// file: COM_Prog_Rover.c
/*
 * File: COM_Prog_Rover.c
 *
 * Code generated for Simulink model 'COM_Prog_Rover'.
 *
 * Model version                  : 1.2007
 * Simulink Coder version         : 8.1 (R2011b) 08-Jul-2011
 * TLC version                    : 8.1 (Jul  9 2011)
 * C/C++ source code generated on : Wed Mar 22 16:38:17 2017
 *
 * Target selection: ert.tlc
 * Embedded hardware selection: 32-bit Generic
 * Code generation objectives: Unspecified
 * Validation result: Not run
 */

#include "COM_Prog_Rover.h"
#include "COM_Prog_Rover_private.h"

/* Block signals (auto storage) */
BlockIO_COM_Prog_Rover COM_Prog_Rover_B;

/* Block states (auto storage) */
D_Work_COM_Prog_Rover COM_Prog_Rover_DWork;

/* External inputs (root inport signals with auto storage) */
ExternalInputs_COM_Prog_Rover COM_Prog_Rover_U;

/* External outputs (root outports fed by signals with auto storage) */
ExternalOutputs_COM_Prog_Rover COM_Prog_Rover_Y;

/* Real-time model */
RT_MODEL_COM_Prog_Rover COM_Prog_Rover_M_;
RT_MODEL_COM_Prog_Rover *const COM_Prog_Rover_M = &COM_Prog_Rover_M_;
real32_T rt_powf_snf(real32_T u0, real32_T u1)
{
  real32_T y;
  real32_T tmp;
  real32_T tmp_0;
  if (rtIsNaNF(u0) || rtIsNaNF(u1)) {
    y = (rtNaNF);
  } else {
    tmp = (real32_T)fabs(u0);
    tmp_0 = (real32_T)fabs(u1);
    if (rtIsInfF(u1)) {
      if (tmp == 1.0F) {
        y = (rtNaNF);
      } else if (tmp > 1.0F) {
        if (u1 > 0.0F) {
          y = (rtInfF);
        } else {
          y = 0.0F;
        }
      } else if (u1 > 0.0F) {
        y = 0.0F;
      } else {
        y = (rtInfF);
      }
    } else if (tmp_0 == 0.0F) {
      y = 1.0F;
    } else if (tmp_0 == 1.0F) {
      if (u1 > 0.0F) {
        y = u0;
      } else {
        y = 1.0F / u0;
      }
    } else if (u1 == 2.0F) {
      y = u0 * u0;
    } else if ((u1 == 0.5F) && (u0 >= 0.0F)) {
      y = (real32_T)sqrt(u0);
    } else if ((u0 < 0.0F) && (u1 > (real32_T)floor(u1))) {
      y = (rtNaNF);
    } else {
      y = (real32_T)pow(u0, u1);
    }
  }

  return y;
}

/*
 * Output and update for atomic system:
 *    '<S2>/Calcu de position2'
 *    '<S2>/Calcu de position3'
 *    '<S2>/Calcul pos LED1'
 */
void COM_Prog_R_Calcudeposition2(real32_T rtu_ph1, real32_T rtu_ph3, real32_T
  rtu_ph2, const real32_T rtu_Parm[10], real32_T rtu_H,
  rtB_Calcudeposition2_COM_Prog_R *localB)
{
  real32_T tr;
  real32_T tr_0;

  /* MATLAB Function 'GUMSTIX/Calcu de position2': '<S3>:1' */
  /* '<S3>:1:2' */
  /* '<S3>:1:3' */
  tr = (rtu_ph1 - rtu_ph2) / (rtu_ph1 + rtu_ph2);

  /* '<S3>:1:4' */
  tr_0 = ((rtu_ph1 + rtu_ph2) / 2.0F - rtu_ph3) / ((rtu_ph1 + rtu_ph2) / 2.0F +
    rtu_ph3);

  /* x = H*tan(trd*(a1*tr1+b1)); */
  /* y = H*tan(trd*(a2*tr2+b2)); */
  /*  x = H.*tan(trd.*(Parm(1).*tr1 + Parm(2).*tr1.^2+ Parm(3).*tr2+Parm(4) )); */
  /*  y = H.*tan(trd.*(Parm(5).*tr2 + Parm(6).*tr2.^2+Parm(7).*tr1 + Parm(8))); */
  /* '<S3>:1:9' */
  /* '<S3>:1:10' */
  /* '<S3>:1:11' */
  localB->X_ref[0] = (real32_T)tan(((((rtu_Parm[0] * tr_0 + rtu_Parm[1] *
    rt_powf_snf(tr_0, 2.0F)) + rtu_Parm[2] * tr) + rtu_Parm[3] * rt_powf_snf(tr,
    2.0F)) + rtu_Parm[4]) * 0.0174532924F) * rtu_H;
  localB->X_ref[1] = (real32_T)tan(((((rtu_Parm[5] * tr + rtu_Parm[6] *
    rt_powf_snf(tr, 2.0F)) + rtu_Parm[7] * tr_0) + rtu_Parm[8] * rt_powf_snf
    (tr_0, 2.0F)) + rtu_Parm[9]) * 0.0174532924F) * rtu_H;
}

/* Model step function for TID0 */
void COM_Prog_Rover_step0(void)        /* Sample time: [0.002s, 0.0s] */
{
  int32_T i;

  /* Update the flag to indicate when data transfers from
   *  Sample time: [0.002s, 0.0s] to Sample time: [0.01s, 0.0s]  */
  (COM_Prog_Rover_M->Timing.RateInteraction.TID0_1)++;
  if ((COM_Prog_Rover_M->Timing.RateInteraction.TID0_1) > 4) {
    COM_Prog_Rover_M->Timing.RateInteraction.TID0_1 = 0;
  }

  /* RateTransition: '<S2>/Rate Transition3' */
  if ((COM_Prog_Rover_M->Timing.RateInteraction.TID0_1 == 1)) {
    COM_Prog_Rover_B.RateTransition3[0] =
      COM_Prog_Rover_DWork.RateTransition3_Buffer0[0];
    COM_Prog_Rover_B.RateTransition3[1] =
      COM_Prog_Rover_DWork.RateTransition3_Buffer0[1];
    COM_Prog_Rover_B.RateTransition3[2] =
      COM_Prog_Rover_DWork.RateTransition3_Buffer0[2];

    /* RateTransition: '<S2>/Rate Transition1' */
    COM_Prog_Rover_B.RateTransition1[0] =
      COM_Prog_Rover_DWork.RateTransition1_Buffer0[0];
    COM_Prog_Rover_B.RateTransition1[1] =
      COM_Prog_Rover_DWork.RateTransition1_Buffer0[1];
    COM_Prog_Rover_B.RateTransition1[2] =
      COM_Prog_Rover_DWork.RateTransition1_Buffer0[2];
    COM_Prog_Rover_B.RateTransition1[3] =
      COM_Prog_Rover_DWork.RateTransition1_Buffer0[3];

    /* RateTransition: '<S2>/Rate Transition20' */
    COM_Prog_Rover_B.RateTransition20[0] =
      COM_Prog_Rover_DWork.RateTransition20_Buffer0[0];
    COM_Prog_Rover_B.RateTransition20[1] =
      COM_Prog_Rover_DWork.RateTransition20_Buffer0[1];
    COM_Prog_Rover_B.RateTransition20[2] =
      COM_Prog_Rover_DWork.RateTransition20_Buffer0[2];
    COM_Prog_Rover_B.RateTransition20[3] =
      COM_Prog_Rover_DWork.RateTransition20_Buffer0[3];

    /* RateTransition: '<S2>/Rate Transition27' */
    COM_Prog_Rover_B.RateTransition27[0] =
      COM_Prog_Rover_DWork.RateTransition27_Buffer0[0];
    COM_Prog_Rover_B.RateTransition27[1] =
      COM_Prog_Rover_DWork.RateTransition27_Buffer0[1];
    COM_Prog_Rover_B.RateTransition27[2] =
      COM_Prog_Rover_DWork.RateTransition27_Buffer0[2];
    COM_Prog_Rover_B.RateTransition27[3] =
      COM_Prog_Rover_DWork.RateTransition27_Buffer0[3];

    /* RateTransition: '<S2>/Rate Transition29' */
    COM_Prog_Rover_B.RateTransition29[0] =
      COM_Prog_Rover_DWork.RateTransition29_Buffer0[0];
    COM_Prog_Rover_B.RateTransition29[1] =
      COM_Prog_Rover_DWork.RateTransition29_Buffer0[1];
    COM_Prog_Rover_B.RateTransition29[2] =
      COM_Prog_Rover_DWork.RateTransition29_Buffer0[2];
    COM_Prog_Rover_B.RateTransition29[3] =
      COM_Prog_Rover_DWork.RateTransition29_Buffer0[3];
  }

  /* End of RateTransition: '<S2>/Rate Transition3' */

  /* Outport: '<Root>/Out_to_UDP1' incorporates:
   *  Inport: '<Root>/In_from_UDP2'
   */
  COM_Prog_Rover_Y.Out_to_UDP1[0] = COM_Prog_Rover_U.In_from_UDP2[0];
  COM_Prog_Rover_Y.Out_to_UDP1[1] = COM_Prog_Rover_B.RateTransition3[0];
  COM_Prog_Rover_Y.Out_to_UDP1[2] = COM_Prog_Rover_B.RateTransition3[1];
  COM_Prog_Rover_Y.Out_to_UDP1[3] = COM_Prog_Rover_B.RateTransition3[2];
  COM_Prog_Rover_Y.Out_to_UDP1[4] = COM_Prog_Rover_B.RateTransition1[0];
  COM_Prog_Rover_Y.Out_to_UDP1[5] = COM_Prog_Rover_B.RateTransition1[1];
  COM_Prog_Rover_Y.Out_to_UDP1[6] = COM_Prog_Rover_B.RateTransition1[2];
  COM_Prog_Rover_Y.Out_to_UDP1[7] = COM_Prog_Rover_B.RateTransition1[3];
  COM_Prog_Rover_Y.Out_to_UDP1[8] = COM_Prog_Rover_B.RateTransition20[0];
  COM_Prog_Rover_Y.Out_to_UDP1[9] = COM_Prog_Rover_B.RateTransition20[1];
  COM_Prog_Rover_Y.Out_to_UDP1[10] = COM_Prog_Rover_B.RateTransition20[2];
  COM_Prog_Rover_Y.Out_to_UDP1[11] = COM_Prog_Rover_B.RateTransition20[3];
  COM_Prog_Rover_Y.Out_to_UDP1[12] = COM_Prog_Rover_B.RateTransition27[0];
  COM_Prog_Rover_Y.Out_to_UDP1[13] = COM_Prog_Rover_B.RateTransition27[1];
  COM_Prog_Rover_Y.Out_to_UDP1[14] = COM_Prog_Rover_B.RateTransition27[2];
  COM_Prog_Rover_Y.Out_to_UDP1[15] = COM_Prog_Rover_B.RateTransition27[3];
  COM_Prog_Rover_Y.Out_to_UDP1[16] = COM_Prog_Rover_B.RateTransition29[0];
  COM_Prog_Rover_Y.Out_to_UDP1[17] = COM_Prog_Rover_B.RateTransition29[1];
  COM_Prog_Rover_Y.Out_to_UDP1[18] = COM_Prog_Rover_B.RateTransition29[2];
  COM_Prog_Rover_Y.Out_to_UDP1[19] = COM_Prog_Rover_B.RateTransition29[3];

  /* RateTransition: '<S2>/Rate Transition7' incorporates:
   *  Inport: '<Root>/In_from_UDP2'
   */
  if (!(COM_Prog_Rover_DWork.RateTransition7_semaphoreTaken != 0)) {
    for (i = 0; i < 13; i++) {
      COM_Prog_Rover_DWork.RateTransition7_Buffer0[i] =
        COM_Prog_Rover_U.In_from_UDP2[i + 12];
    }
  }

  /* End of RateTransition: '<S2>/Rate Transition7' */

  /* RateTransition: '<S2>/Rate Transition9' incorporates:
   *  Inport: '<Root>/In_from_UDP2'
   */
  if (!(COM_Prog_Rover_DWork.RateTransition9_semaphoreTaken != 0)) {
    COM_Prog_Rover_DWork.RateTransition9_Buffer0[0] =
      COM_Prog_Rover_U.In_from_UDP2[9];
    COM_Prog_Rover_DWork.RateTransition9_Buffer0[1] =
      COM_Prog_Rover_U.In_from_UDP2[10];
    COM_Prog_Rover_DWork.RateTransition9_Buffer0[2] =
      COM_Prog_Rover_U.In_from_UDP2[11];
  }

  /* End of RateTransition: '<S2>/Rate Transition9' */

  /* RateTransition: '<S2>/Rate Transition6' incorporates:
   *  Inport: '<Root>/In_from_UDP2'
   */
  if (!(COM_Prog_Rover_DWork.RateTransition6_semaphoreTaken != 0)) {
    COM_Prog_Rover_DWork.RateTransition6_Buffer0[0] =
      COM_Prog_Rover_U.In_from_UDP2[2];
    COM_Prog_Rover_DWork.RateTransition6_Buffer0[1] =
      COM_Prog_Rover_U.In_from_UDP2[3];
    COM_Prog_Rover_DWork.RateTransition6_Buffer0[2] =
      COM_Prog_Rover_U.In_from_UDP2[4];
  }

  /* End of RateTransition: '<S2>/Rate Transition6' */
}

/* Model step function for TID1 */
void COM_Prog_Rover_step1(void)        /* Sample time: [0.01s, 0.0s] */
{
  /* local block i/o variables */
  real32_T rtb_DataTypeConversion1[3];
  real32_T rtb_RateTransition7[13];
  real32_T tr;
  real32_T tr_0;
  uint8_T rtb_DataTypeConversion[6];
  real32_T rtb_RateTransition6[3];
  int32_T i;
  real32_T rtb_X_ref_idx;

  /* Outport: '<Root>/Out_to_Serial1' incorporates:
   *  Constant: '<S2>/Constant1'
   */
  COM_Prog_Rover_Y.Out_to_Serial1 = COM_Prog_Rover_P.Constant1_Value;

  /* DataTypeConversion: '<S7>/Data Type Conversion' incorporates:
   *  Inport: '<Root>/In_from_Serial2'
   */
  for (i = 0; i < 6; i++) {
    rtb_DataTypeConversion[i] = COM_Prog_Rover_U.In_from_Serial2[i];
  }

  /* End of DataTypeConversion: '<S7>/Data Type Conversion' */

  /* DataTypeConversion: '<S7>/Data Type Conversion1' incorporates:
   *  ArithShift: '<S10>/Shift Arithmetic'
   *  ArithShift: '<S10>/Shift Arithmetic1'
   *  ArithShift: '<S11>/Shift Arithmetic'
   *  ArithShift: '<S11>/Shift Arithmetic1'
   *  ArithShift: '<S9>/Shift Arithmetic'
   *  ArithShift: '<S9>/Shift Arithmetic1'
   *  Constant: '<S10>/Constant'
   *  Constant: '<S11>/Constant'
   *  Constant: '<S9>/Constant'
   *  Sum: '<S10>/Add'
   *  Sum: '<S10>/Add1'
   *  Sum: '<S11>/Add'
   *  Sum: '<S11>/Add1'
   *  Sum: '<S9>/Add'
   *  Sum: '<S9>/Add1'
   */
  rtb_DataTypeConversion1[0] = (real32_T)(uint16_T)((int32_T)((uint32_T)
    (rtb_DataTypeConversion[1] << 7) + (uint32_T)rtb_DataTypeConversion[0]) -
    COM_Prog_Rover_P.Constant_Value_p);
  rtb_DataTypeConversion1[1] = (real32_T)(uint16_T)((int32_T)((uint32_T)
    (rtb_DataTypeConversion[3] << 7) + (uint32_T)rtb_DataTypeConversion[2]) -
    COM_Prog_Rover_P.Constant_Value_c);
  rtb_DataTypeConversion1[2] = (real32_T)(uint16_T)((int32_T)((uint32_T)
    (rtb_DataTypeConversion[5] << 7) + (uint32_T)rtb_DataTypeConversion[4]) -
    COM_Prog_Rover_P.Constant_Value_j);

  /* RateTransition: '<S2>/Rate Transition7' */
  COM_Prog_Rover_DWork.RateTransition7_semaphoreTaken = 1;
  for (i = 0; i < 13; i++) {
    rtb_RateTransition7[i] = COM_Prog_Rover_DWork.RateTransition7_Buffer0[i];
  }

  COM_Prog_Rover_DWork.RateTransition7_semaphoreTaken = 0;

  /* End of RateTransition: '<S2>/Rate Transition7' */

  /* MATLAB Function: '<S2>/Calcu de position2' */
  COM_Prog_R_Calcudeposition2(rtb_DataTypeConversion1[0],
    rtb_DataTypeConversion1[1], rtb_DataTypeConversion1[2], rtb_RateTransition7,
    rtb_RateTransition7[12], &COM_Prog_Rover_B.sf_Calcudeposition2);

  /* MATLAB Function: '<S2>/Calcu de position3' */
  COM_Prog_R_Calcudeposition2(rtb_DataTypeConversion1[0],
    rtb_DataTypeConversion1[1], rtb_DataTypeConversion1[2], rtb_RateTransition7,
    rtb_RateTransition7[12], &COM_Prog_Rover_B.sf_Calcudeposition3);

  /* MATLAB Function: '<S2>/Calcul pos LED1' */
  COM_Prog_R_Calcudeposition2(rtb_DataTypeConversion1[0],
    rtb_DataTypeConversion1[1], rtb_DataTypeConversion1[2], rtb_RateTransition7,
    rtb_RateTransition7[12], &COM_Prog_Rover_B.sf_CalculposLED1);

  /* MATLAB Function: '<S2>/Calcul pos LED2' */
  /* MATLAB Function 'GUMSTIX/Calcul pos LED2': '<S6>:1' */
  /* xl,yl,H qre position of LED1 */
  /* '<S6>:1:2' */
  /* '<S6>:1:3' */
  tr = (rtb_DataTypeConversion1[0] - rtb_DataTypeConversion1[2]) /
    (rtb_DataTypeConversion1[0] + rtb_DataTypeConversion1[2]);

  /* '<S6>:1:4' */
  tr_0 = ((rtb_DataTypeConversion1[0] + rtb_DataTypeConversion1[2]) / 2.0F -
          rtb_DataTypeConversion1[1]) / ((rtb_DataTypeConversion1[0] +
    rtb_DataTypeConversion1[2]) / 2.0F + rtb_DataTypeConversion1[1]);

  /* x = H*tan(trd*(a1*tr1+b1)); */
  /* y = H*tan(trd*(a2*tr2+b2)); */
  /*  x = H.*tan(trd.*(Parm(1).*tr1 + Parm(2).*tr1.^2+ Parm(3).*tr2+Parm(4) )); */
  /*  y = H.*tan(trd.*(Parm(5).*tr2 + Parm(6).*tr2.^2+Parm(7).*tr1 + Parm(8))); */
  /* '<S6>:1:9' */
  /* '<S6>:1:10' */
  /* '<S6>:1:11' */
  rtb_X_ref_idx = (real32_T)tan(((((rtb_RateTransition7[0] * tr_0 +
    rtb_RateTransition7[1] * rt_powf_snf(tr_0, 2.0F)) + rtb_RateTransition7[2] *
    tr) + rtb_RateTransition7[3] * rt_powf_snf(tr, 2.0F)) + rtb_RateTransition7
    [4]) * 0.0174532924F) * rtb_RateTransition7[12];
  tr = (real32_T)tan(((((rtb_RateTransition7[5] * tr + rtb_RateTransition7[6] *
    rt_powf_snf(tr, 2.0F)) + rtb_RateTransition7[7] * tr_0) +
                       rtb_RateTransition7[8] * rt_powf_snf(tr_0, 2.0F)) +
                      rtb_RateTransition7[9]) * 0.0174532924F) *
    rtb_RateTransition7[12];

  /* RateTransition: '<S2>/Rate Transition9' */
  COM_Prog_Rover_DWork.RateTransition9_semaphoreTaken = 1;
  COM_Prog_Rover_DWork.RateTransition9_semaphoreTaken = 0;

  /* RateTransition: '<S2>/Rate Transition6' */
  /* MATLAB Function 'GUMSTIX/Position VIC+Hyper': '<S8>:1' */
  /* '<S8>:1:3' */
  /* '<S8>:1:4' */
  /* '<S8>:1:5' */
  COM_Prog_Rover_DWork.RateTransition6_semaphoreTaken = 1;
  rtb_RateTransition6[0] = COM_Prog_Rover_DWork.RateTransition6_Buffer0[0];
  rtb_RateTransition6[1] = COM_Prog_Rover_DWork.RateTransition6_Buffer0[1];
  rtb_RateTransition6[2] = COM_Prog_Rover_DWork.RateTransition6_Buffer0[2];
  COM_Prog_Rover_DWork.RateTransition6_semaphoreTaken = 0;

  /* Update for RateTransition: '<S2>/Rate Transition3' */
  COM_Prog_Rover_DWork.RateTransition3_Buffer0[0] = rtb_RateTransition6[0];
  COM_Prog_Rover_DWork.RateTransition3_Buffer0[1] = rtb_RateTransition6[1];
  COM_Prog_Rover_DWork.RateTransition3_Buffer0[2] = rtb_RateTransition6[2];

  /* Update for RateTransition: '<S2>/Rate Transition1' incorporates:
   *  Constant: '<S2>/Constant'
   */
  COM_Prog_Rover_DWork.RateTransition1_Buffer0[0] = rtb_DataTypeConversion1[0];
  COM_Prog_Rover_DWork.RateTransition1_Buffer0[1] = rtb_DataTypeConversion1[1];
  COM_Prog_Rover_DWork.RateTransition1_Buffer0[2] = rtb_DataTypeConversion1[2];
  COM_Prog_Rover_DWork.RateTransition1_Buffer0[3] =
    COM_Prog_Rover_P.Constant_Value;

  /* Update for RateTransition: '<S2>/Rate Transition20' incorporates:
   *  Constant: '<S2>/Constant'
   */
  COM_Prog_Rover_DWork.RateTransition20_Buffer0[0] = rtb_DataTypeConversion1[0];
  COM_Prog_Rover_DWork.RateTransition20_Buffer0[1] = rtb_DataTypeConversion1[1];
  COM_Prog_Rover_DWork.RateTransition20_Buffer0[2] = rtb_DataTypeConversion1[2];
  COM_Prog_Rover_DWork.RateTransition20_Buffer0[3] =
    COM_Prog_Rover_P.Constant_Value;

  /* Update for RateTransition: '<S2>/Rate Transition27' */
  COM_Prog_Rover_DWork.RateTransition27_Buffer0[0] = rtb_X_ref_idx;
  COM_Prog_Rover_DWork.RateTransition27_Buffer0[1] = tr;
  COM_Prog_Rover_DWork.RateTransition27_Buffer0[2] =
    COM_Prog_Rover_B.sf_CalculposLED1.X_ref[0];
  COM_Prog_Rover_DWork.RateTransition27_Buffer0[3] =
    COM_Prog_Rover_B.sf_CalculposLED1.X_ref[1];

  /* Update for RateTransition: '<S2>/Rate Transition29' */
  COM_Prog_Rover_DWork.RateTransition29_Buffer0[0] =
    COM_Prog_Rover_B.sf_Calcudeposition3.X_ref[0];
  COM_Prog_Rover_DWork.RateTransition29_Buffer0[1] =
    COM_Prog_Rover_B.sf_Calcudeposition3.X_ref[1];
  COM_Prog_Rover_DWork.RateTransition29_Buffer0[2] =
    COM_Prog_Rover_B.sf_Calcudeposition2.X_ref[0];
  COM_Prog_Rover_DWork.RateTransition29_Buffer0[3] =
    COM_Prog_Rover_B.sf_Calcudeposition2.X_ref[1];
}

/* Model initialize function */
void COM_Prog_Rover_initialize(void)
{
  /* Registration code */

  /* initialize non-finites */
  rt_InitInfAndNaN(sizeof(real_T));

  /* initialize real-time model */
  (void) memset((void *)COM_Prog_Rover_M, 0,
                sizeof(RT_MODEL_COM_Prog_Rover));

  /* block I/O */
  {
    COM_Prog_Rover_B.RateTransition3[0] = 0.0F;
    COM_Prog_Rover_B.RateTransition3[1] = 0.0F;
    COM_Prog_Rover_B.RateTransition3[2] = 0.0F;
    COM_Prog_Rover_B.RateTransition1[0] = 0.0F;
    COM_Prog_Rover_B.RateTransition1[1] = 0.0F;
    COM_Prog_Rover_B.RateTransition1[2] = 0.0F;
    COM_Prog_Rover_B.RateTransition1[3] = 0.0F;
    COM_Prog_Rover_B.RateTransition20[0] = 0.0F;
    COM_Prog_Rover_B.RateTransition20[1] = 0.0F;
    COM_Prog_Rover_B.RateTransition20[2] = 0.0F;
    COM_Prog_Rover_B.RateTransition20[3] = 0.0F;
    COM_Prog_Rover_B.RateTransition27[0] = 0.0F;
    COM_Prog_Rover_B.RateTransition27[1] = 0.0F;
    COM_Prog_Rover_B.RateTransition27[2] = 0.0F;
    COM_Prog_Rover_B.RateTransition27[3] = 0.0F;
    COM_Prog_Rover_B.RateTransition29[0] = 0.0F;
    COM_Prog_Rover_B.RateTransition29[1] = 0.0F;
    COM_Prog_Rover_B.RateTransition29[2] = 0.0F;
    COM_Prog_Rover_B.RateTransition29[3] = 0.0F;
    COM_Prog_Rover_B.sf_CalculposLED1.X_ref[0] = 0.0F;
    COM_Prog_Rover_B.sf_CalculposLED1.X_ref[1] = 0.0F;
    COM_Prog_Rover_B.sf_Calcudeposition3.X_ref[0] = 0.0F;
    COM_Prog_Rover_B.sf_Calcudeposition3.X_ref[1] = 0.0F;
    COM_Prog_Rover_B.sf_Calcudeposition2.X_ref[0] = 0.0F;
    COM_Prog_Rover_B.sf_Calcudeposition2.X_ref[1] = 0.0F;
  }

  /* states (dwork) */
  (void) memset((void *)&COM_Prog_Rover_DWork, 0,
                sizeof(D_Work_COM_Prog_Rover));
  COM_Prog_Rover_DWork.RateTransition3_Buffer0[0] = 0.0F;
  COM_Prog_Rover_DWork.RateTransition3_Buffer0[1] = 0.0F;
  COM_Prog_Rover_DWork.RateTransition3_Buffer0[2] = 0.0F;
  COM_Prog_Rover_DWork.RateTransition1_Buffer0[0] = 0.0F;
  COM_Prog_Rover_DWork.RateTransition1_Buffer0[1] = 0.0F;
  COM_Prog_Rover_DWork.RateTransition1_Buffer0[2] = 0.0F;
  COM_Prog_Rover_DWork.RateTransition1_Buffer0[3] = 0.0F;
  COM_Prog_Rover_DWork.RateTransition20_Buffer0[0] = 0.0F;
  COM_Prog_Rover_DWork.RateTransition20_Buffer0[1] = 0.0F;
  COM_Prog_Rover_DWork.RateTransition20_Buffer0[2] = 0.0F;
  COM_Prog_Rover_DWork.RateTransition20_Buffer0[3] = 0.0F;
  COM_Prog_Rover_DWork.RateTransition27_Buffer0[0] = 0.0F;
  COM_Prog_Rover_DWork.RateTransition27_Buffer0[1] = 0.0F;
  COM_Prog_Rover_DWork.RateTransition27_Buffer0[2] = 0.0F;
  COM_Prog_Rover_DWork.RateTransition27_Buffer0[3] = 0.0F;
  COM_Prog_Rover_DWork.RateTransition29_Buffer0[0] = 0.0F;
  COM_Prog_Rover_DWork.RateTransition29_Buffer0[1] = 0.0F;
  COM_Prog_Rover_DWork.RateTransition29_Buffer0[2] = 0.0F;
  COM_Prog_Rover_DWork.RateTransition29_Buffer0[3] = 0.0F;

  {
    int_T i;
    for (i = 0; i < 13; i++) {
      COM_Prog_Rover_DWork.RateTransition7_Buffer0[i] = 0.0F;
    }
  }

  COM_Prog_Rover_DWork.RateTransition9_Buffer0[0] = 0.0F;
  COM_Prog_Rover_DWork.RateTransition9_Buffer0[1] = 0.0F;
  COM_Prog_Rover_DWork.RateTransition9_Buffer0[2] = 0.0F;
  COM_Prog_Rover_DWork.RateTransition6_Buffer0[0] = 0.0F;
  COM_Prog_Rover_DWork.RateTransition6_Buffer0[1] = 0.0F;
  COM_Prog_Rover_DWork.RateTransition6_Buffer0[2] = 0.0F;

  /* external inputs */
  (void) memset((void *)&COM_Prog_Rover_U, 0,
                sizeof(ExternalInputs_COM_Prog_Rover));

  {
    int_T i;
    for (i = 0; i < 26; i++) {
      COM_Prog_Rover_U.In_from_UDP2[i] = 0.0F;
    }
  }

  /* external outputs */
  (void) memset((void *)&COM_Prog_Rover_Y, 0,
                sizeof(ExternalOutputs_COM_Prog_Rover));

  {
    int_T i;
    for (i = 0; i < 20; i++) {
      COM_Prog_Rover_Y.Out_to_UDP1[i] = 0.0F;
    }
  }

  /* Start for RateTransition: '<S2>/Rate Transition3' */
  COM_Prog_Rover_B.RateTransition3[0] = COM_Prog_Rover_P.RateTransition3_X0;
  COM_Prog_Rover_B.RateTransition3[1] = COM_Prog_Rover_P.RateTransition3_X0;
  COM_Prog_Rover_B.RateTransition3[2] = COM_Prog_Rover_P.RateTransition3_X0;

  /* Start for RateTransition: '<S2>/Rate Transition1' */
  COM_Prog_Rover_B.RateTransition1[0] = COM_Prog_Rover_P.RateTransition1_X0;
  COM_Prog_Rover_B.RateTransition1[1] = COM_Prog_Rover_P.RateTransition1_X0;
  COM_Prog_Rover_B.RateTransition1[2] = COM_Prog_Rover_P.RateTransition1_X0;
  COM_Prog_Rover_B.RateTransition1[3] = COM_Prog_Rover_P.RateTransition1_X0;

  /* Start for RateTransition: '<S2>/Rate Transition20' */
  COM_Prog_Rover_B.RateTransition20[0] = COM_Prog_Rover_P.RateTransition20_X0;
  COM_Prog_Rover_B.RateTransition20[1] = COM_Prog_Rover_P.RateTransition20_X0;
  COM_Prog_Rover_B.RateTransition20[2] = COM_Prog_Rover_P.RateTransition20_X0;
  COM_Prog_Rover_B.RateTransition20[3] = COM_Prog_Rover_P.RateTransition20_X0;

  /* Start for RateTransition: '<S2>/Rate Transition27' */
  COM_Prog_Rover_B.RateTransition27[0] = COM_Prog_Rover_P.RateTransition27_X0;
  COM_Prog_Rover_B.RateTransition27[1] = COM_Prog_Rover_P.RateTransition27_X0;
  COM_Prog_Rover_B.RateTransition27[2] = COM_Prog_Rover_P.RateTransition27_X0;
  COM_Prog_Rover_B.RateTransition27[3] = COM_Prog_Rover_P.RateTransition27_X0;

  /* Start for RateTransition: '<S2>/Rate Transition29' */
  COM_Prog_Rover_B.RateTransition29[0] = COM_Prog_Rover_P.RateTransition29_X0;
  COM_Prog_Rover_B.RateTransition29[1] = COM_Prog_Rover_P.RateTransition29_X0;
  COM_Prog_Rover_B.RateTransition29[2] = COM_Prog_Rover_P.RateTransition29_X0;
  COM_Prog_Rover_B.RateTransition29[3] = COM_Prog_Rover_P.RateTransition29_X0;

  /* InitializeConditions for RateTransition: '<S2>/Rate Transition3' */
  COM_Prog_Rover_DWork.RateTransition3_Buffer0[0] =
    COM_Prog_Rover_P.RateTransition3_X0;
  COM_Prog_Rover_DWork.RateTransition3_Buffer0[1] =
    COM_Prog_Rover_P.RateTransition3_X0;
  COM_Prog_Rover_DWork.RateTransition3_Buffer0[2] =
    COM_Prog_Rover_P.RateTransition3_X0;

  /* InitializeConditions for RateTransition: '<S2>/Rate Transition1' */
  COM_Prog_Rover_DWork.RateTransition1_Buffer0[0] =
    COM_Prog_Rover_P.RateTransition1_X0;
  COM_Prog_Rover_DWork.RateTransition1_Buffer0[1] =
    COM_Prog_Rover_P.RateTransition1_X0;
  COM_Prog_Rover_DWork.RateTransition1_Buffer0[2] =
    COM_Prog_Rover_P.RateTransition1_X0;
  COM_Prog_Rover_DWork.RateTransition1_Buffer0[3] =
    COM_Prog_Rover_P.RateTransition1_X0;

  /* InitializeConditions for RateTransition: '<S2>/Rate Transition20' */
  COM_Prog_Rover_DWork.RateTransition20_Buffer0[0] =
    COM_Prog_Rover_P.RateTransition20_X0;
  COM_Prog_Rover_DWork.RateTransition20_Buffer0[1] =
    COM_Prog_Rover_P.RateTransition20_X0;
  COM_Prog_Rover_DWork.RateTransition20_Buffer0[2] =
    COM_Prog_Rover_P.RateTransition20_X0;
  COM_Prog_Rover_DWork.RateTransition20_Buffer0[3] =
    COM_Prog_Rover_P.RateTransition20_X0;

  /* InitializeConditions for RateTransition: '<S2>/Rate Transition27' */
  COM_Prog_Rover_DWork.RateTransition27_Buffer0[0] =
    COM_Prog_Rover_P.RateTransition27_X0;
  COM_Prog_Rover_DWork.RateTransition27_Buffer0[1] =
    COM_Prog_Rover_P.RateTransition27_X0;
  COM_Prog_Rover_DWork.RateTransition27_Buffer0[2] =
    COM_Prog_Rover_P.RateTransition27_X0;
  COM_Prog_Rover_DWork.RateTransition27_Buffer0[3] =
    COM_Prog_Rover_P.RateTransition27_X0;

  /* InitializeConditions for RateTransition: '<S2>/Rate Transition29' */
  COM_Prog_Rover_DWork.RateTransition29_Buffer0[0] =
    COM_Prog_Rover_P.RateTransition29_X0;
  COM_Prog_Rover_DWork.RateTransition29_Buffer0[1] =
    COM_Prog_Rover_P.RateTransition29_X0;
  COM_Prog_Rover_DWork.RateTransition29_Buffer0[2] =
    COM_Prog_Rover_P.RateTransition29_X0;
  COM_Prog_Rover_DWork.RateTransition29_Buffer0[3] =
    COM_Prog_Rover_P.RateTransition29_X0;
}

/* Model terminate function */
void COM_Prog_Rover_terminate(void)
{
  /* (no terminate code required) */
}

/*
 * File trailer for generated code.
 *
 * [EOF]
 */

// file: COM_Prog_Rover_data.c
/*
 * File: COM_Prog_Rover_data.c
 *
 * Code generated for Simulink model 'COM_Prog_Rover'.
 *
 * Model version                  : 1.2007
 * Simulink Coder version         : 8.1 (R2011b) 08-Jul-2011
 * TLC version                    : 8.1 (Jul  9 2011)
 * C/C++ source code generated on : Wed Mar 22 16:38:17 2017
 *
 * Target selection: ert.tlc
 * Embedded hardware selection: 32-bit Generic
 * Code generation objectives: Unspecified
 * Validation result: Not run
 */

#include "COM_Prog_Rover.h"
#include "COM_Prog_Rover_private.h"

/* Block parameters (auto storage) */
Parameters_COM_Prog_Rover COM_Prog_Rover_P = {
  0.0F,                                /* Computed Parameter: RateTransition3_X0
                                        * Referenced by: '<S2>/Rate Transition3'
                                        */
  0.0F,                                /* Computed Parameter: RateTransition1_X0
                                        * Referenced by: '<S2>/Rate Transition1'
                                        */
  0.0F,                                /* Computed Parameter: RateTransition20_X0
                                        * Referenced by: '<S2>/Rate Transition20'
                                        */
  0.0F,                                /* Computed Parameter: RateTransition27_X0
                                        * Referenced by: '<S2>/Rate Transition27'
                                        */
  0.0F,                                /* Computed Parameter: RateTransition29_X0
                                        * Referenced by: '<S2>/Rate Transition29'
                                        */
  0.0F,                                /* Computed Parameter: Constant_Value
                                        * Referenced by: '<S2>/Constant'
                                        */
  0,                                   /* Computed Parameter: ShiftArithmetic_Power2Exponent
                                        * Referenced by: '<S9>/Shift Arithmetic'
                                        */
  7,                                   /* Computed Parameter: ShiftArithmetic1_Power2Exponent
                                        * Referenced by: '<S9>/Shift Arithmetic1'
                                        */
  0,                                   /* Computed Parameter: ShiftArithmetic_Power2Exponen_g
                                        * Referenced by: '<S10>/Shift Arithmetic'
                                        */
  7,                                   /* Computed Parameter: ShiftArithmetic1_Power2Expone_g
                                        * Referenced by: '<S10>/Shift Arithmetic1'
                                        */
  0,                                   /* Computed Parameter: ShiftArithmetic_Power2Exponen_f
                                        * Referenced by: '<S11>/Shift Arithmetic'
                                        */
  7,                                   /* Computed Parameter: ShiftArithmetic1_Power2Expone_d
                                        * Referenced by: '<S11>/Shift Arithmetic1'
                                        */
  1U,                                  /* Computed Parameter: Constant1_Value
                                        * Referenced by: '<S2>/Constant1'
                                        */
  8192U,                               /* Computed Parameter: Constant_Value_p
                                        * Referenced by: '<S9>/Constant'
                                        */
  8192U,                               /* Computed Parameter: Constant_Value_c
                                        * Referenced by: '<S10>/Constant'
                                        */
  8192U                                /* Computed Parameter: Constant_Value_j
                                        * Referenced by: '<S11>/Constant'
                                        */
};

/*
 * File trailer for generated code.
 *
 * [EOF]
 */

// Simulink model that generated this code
simulink model "COM_Prog_Rover"  (Simulink 7.8)
settings: Solver=FixedStepDiscrete  StartTime=0.0  StopTime=inf  FixedStep=ComMinSampleTime  RelTol=1e-3
undefined symbols (not defined in the file or in its folder): ComMinSampleTime, Gumstix

== system COM_Prog_Rover ==
  In_from_UDP2 : Inport  OutDataTypeStr=single  PortDimensions=Gumstix.UDP.Reception(1).NbData  SampleTime=Gumstix.UDP.Reception(1).SampleTime  mask{UDP_NbData=26, UDP_DataType=float32, UDP_remoteIPaddress='192.168.137.3', UDP_remotePort=2012, UDP_Interface=wlan0, UDP_localPort=2012, UDP_SampleTime=ComMinSampleTime, UDP_BlockingReception=OFF (try to read the n data), UDP_BlockingTimeOut=0.1}
      mask prompts: UDP_NbData "Number of Received Data"; UDP_DataType "UDP Data Type"; UDP_remoteIPaddress "Remote peer's IP address (IPv4)"; UDP_remotePort "Remote peer's Port (1023<port<65536)"; UDP_Interface "Local Interface to use"; UDP_localPort "Local Port (1023<port<65536)"; UDP_SampleTime "Reception Sample Time [s]"; UDP_BlockingReception "Blocking Reception"; UDP_BlockingTimeOut "Blocking Time Out [s]"
      mask init:
      | for i=1:1:8
      |     ProcessUDPInportMask_COM(gcb, i);
      | end
  In_from_Serial2 : Inport  Port=2  OutDataTypeStr=uint8  PortDimensions=Gumstix.RS232.Reception(1).NbData  SampleTime=Gumstix.RS232.Reception(1).SampleTime  mask{RS232_NbData=6, RS232_DataType=unsigned char8, RS232_Port=/dev/ttyO0, RS232_BaudRate=115200, RS232_SampleTime=0.01, RS232_BlockingReception=OFF (try to read the n data), RS232_BlockingTimeOut=0.00022, RS232_StreamHeaderReception=1 byte, RS232_StreamHeaderValue=174, RS232_StartProtocol=SendStart -> WaitStart, RS232_StartTimeOut=100, RS232_StartStream=START, RS232_StopProtocol=None, RS232_StopTimeOut=100, RS232_StopStream=STOP}
      mask prompts: RS232_NbData "Number of Received Data"; RS232_DataType "RS232 Data Type"; RS232_Port "Serial Port"; RS232_BaudRate "BaudRate"; RS232_SampleTime "Reception Sample Time [s]"; RS232_BlockingReception "Blocking Reception"; RS232_BlockingTimeOut "Blocking Time Out [s]"; RS232_StreamHeaderReception "Stream Header"; RS232_StreamHeaderValue "Stream header value [0-255]"; RS232_StartProtocol "START Protocols"; RS232_StartTimeOut "Start Stream Waiting TimeOut [ms]"; RS232_StartStream "Start Message"; RS232_StopProtocol "STOP Protocols"; RS232_StopTimeOut "Stop Stream Waiting TimeOut [ms]"; RS232_StopStream "Stop Message"
      mask init:
      | for i=1:1:15
      |     ProcessRS232InportMask_COM(gcb, i);
      | end
  DisplaySampleTimeColors : Subsystem  mask{SampleTime_1=0.002, SampleTime_2=0.004, SampleTime_3=0.01}
  GUMSTIX : Subsystem
  Gumstix Configuration : Subsystem  mask{TimeSynchro=Internal Clock, RS232_InterruptSource=/dev/ttyO0, UDP_InterruptSource=wlan0, PrintfMode=off, FprintfMode=off, TimeLoggerMode=off, PrintfTimeMode=off, FprintfTimeMode=off, TaskingMode=Multi-Tasking, SchedPolicy=SCHED_RR        (Real-Time Scheduler), MaxTaskPriority=96, RTsystem=PREEMPT-RT}
      mask prompts: TimeSynchro "Time Scheduler"; RS232_InterruptSource "RS232 Interrupt Source"; UDP_InterruptSource "UDP Interrupt Source"; PrintfMode "Verbose mode activated in the Gumstix console"; FprintfMode "Verbose mode logged in a file (onto Gumstix)"; TimeLoggerMode "Time logger mode activated (log time exec of each task)"; PrintfTimeMode "Execution time plotted in the Gumstix console"; FprintfTimeMode "Execution time logged in a file (onto Gumstix)"; TaskingMode "Tasking Mode"; SchedPolicy "Scheduler Policy"; MaxTaskPriority "Maximum Task Priority [1-99]"; RTsystem "RT system"
      mask init:
      | for i=1:1:12
      |     ProcessConfigMask_COM(gcb, i);
      | end
  Out_to_UDP1 : Outport  OutDataTypeStr=single  PortDimensions=Gumstix.UDP.Emission(1).NbData  SampleTime=Gumstix.UDP.Emission(1).SampleTime  mask{UDP_NbData=20, UDP_DataType=float32, UDP_RemoteIPaddress='192.168.137.3', UDP_RemotePort=2012, UDP_Interface=wlan0, UDP_LocalPort=2012, UDP_SampleTime=ComMinSampleTime}
      mask prompts: UDP_NbData "Number of Sent Data"; UDP_DataType "UDP Data Type"; UDP_RemoteIPaddress "remote peer's IP address (IPv4)"; UDP_RemotePort "remote peer's Port (1023<port<65536)"; UDP_Interface "Local Interface to use for UDP"; UDP_LocalPort "Local port to use"; UDP_SampleTime "Emission Sample Time [s]"
      mask init:
      | for i=1:1:7
      |     ProcessUDPOutportMask_COM(gcb, i);
      | end
  Out_to_Serial1 : Outport  Port=2  OutDataTypeStr=uint16  PortDimensions=Gumstix.RS232.Emission(1).NbData  SampleTime=Gumstix.RS232.Emission(1).SampleTime  mask{RS232_NbData=1, RS232_DataType=unsigned int16, RS232_Port=/dev/ttyO0, RS232_BaudRate=115200, RS232_SampleTime=0.01, RS232_StreamHeaderReception=1 byte, RS232_StreamHeaderValue=174, RS232_StartProtocol=SendStart -> WaitStart, RS232_StartTimeOut=100, RS232_StartStream=START, RS232_StopProtocol=None, RS232_StopTimeOut=100, RS232_StopStream=STOP}
      mask prompts: RS232_NbData "Number of Sent Data"; RS232_DataType "RS232 Data Type"; RS232_Port "Serial Port"; RS232_BaudRate "BaudRate"; RS232_SampleTime "Sample Time [s]"; RS232_StreamHeaderReception "Stream Header"; RS232_StreamHeaderValue "Stream header value [0-255]"; RS232_StartProtocol "RS232 Start Protocol"; RS232_StartTimeOut "Start Stream Waiting TimeOut [ms]"; RS232_StartStream "Start Message"; RS232_StopProtocol "RS232 Stop Protocol"; RS232_StopTimeOut "Stop Stream Waiting TimeOut [ms]"; RS232_StopStream "Stop Message"
      mask init:
      | for i=1:1:13
      |     ProcessRS232OutportMask_COM(gcb, i);
      | end
  wires:
  GUMSTIX/1(Out_to_UDP) -> Out_to_UDP1/1
  In_from_UDP2/1 -> GUMSTIX/1(In_from_UDP)
  In_from_Serial2/1 -> GUMSTIX/2("In_from_Serial2 ")
  GUMSTIX/2(Out_to_Serial) -> Out_to_Serial1/1

== system COM_Prog_Rover/DisplaySampleTimeColors ==
  Constant : Constant  OutDataTypeStr=uint8
  Gain : Gain
  Terminator : Terminator
  wires:
  Constant/1 -> Gain/1
  Gain/1 -> Terminator/1

== system COM_Prog_Rover/GUMSTIX ==
  note: enable rotation detec
  note: 0.002
  note: 0.002
  note: 0.01
  note: 0.01
  note: 0.01
  note: 0.01
  note: 0.01
  note: ??
  In_from_UDP : Inport
  "In_from_Serial2 " : Inport  Port=2
  Calcu de position2 : MATLAB Function  TreatAsAtomicUnit=on
  Calcu de position3 : MATLAB Function  TreatAsAtomicUnit=on
  Calcul pos LED1 : MATLAB Function  TreatAsAtomicUnit=on
  Calcul pos LED2 : MATLAB Function  TreatAsAtomicUnit=on
  Constant : Constant  Value=0  OutDataTypeStr=Inherit: Inherit via back propagation  SampleTime=0.01
  Constant1 : Constant  OutDataTypeStr=Inherit: Inherit via back propagation  SampleTime=0.01
  Data Type Conversion2 : DataTypeConversion
  Data Type Conversion3 : DataTypeConversion
  Data Type Conversion5 : DataTypeConversion
  Decode1 : Subsystem
  Demux : Demux  Outputs=[2 1]
  Demux{1,4,9,12} (4 alike) : Demux  Outputs=[10 1 1 1]
  Demux10 : Demux  Outputs=[ 1 1 1 1]
  Demux13 : Demux  Outputs=[ 1 1 1 1]
  Demux18 : Demux  Outputs=[1 1]
  Demux2 : Demux  Outputs=[1 1 1 1]
  Demux5 : Demux  Outputs=[1 1 1 1]
  In_from_UDP_Demux : Demux  Outputs=[1 1 3 3 1 3 13 1]
  Mux : Mux  Inputs=2
  Mux2 : Mux  Inputs=2
  Mux4 : Mux  Inputs=2
  Out_to_UDP_Mux : Mux  Inputs=[1 3 4 4 4 4]
  Position VIC+Hyper : MATLAB Function  TreatAsAtomicUnit=on
  Rate Transition{1,3,20,27,29} (5 alike) : RateTransition
  Rate Transition2 : RateTransition  Deterministic=off
  Rate Transition{6..7,9,23,31} (5 alike) : RateTransition  Deterministic=off  OutPortSampleTime=Ts_control
  Rate Transition24 : RateTransition  Deterministic=off
  Out_to_UDP : Outport
  Out_to_Serial : Outport  Port=2
  wires:
  In_from_UDP/1 -> Rate Transition2/1
  Rate Transition2/1 -> Data Type Conversion3/1
  Data Type Conversion3/1 -> In_from_UDP_Demux/1
  In_from_UDP_Demux/1 -> [Compteur]
  In_from_UDP_Demux/2 -> [Mode]
  Rate Transition9/1 -> [States]
  [References] -> Rate Transition3/1
  Rate Transition6/1 -> [References]
  Rate Transition23/1 -> [X_mes]
  Rate Transition24/1 -> [Int_reset]
  Rate Transition3/1 -> Out_to_UDP_Mux/2
  Demux1/1 -> Calcul pos LED1/4(Parm)
  Rate Transition7/1 -> [par_loc]
  Demux1/2 -> Calcul pos LED1/5(xl)
  Demux1/3 -> Calcul pos LED1/6(yl)
  Demux1/4 -> [H], Calcul pos LED1/7(H)
  [Capteur2] -> Rate Transition20/1
  [par_loc] -> Demux4/1
  Demux4/1 -> Calcul pos LED2/4(Parm)
  Demux4/2 -> Calcul pos LED2/5(xl)
  Demux4/3 -> Calcul pos LED2/6(yl)
  Demux4/4 -> Calcul pos LED2/7(H)
  [Capteur2] -> Demux2/1
  Calcul pos LED2/1(X_ref) -> [X_est_2]
  [Compteur] -> Out_to_UDP_Mux/1
  Out_to_UDP_Mux/1 -> Out_to_UDP/1
  [X_est_2] -> Mux2/1
  Mux2/1 -> Data Type Conversion2/1
  Data Type Conversion2/1 -> Rate Transition27/1
  [X_est_1] -> Mux2/2
  Position VIC+Hyper/1(X_new) -> [X_mes_hybride]
  [Capteur1] -> Rate Transition1/1
  [States] -> Demux/1
  Demux9/1 -> Calcu de position2/4(Parm)
  [par_loc] -> Demux9/1
  Demux9/2 -> Calcu de position2/5(xl)
  Demux9/3 -> Calcu de position2/6(yl)
  Demux9/4 -> Calcu de position2/7(H)
  [Capteur1] -> Demux13/1
  [par_loc] -> Demux12/1
  Demux12/1 -> Calcu de position3/4(Parm)
  Demux12/2 -> Calcu de position3/5(xl)
  Demux12/3 -> Calcu de position3/6(yl)
  Demux12/4 -> Calcu de position3/7(H)
  [Capteur2] -> Demux10/1
  Calcu de position3/1(X_ref) -> [X_est_2_b]
  Demux10/1 -> Calcu de position3/1(ph1)
  Demux10/2 -> Calcu de position3/2(ph3)
  Demux10/3 -> Calcu de position3/3(ph2)
  Demux13/1 -> Calcu de position2/1(ph1)
  Demux13/2 -> Calcu de position2/2(ph3)
  Demux13/3 -> Calcu de position2/3(ph2)
  Calcul pos LED1/1(X_ref) -> Demux18/1, [X_est_1]
  [X_est_2_b] -> Mux4/1
  Mux4/1 -> Data Type Conversion5/1
  Data Type Conversion5/1 -> Rate Transition29/1
  [X_est_1_b] -> Mux4/2
  Rate Transition31/1 -> [d]
  Demux18/2 -> Position VIC+Hyper/2(y_hyp)
  Demux18/1 -> Position VIC+Hyper/1(x_hyp)
  Demux/2 -> Position VIC+Hyper/3(phi_vic)
  [par_loc] -> Demux1/1
  [Capteur1] -> Demux5/1
  Calcu de position2/1(X_ref) -> [X_est_1_b]
  Rate Transition1/1 -> Out_to_UDP_Mux/3
  In_from_UDP_Demux/3 -> Rate Transition6/1
  In_from_UDP_Demux/4 -> Rate Transition23/1
  In_from_UDP_Demux/5 -> Rate Transition24/1
  In_from_UDP_Demux/6 -> Rate Transition9/1
  In_from_UDP_Demux/7 -> Rate Transition7/1
  In_from_UDP_Demux/8 -> Rate Transition31/1
  Rate Transition20/1 -> Out_to_UDP_Mux/4
  Rate Transition27/1 -> Out_to_UDP_Mux/5
  Rate Transition29/1 -> Out_to_UDP_Mux/6
  "In_from_Serial2 "/1 -> Decode1/1(In1)
  Decode1/1(Out1) -> Mux/1
  Constant/1 -> Mux/2
  Mux/1 -> [Capteur1], [Capteur2]
  Demux2/1 -> Calcul pos LED2/1(ph1)
  Demux2/2 -> Calcul pos LED2/2(ph3)
  Demux2/3 -> Calcul pos LED2/3(ph2)
  Demux5/1 -> Calcul pos LED1/1(ph1)
  Demux5/2 -> Calcul pos LED1/2(ph3)
  Demux5/3 -> Calcul pos LED1/3(ph2)
  Constant1/1 -> Out_to_Serial/1

== system COM_Prog_Rover/Gumstix Configuration ==

== system COM_Prog_Rover/GUMSTIX/Decode1 ==
  In1 : Inport
  Data Type Conversion : DataTypeConversion  OutDataTypeStr=uint16
  Data Type Conversion1 : DataTypeConversion  OutDataTypeStr=single
  Demux : Demux  Outputs=6
  Mux : Mux  Inputs=3
  Subsystem : Subsystem
  Subsystem1 : Subsystem
  Subsystem2 : Subsystem
  Out1 : Outport
  wires:
  Data Type Conversion1/1 -> Out1/1
  In1/1 -> Data Type Conversion/1
  Data Type Conversion/1 -> Demux/1
  Demux/1 -> Subsystem/1(In1)
  Demux/2 -> Subsystem/2(In2)
  Demux/3 -> Subsystem1/1(In1)
  Demux/4 -> Subsystem1/2(In2)
  Demux/5 -> Subsystem2/1(In1)
  Demux/6 -> Subsystem2/2(In2)
  Subsystem/1(Out1) -> Mux/1
  Subsystem1/1(Out1) -> Mux/2
  Subsystem2/1(Out1) -> Mux/3
  Mux/1 -> Data Type Conversion1/1

== system COM_Prog_Rover/GUMSTIX/Decode1/Subsystem ==
  In1 : Inport
  In2 : Inport  Port=2
  Add : Sum
  Add1 : Sum  Inputs=+-
  Constant : Constant  Value=2^13  OutDataTypeStr=uint16  SampleTime=-1
  Shift Arithmetic : ArithShift  BitShiftDirection=Right
  Shift Arithmetic1 : ArithShift  BitShiftNumber=7  BitShiftDirection=Left
  Out1 : Outport
  wires:
  In1/1 -> Shift Arithmetic/1
  In2/1 -> Shift Arithmetic1/1
  Shift Arithmetic/1 -> Add/1
  Shift Arithmetic1/1 -> Add/2
  Add/1 -> Add1/1
  Constant/1 -> Add1/2
  Add1/1 -> Out1/1

== system COM_Prog_Rover/GUMSTIX/Decode1/Subsystem1 ==
  In1 : Inport
  In2 : Inport  Port=2
  Add : Sum
  Add1 : Sum  Inputs=+-
  Constant : Constant  Value=2^13  OutDataTypeStr=uint16  SampleTime=-1
  Shift Arithmetic : ArithShift  BitShiftDirection=Right
  Shift Arithmetic1 : ArithShift  BitShiftNumber=7  BitShiftDirection=Left
  Out1 : Outport
  wires:
  In1/1 -> Shift Arithmetic/1
  In2/1 -> Shift Arithmetic1/1
  Shift Arithmetic/1 -> Add/1
  Shift Arithmetic1/1 -> Add/2
  Add/1 -> Add1/1
  Constant/1 -> Add1/2
  Add1/1 -> Out1/1

== system COM_Prog_Rover/GUMSTIX/Decode1/Subsystem2 ==
  In1 : Inport
  In2 : Inport  Port=2
  Add : Sum
  Add1 : Sum  Inputs=+-
  Constant : Constant  Value=2^13  OutDataTypeStr=uint16  SampleTime=-1
  Shift Arithmetic : ArithShift  BitShiftDirection=Right
  Shift Arithmetic1 : ArithShift  BitShiftNumber=7  BitShiftDirection=Left
  Out1 : Outport
  wires:
  In1/1 -> Shift Arithmetic/1
  In2/1 -> Shift Arithmetic1/1
  Shift Arithmetic/1 -> Add/1
  Shift Arithmetic1/1 -> Add/2
  Add/1 -> Add1/1
  Constant/1 -> Add1/2
  Add1/1 -> Out1/1

== matlab function GUMSTIX/Calcul pos LED2 ==
function X_ref = position(ph1, ph3, ph2, Parm, xl, yl, H)   %xl,yl,H qre position of LED1
trd = pi/180;
tr2 = (ph1-ph2)/(ph1+ph2);
tr1 = (((ph1+ph2)/2)-ph3)/(((ph1+ph2)/2)+ph3);
%x = H*tan(trd*(a1*tr1+b1));
%y = H*tan(trd*(a2*tr2+b2));
% x = H.*tan(trd.*(Parm(1).*tr1 + Parm(2).*tr1.^2+ Parm(3).*tr2+Parm(4) ));
% y = H.*tan(trd.*(Parm(5).*tr2 + Parm(6).*tr2.^2+Parm(7).*tr1 + Parm(8)));
x = H.*tan(trd.*(Parm(1).*tr1 + Parm(2).*tr1.^2+ Parm(3).*tr2+  Parm(4).*tr2.^2+Parm(5) ));
y = H.*tan(trd.*(Parm(6).*tr2 + Parm(7).*tr2.^2+Parm(8).*tr1 + Parm(9).*tr1.^2+Parm(10)));
X_ref = [x,y];
end

== matlab function GUMSTIX/Calcu de position2 ==
function X_ref = position(ph1, ph3, ph2, Parm, xl, yl, H)
trd = pi/180;
tr2 = (ph1-ph2)/(ph1+ph2);
tr1 = (((ph1+ph2)/2)-ph3)/(((ph1+ph2)/2)+ph3);
%x = H*tan(trd*(a1*tr1+b1));
%y = H*tan(trd*(a2*tr2+b2));
% x = H.*tan(trd.*(Parm(1).*tr1 + Parm(2).*tr1.^2+ Parm(3).*tr2+Parm(4) ));
% y = H.*tan(trd.*(Parm(5).*tr2 + Parm(6).*tr2.^2+Parm(7).*tr1 + Parm(8)));
x = H.*tan(trd.*(Parm(1).*tr1 + Parm(2).*tr1.^2+ Parm(3).*tr2+  Parm(4).*tr2.^2+Parm(5) ));
y = H.*tan(trd.*(Parm(6).*tr2 + Parm(7).*tr2.^2+Parm(8).*tr1 + Parm(9).*tr1.^2+Parm(10)));
X_ref = [x,y];
end

== matlab function GUMSTIX/Calcul pos LED1 ==
function X_ref = position(ph1, ph3, ph2, Parm, xl, yl, H)
trd = pi/180;
tr2 = (ph1-ph2)/(ph1+ph2);
tr1 = (((ph1+ph2)/2)-ph3)/(((ph1+ph2)/2)+ph3);
%x = H*tan(trd*(a1*tr1+b1));
%y = H*tan(trd*(a2*tr2+b2));
% x = H.*tan(trd.*(Parm(1).*tr1 + Parm(2).*tr1.^2+ Parm(3).*tr2+Parm(4) ));
% y = H.*tan(trd.*(Parm(5).*tr2 + Parm(6).*tr2.^2+Parm(7).*tr1 + Parm(8)));
x = H.*tan(trd.*(Parm(1).*tr1 + Parm(2).*tr1.^2+ Parm(3).*tr2+  Parm(4).*tr2.^2+Parm(5) ));
y = H.*tan(trd.*(Parm(6).*tr2 + Parm(7).*tr2.^2+Parm(8).*tr1 + Parm(9).*tr1.^2+Parm(10)));
X_ref = [x,y];
end

== matlab function GUMSTIX/Calcu de position3 ==
function X_ref = position(ph1, ph3, ph2, Parm, xl, yl, H)
trd = pi/180;
tr2 = (ph1-ph2)/(ph1+ph2);
tr1 = (((ph1+ph2)/2)-ph3)/(((ph1+ph2)/2)+ph3);
%x = H*tan(trd*(a1*tr1+b1));
%y = H*tan(trd*(a2*tr2+b2));
% x = H.*tan(trd.*(Parm(1).*tr1 + Parm(2).*tr1.^2+ Parm(3).*tr2+Parm(4) ));
% y = H.*tan(trd.*(Parm(5).*tr2 + Parm(6).*tr2.^2+Parm(7).*tr1 + Parm(8)));
x = H.*tan(trd.*(Parm(1).*tr1 + Parm(2).*tr1.^2+ Parm(3).*tr2+  Parm(4).*tr2.^2+Parm(5) ));
y = H.*tan(trd.*(Parm(6).*tr2 + Parm(7).*tr2.^2+Parm(8).*tr1 + Parm(9).*tr1.^2+Parm(10)));
X_ref = [x,y];
end

== matlab function GUMSTIX/Position VIC+Hyper ==
function X_new = position(x_hyp, y_hyp, phi_vic)
phi = phi_vic;
A = [cos(phi) -sin(phi) 0; sin(phi) cos(phi) 0; 0 0 1];
X = A*[x_hyp;y_hyp;phi_vic];
X_new = X';
end
